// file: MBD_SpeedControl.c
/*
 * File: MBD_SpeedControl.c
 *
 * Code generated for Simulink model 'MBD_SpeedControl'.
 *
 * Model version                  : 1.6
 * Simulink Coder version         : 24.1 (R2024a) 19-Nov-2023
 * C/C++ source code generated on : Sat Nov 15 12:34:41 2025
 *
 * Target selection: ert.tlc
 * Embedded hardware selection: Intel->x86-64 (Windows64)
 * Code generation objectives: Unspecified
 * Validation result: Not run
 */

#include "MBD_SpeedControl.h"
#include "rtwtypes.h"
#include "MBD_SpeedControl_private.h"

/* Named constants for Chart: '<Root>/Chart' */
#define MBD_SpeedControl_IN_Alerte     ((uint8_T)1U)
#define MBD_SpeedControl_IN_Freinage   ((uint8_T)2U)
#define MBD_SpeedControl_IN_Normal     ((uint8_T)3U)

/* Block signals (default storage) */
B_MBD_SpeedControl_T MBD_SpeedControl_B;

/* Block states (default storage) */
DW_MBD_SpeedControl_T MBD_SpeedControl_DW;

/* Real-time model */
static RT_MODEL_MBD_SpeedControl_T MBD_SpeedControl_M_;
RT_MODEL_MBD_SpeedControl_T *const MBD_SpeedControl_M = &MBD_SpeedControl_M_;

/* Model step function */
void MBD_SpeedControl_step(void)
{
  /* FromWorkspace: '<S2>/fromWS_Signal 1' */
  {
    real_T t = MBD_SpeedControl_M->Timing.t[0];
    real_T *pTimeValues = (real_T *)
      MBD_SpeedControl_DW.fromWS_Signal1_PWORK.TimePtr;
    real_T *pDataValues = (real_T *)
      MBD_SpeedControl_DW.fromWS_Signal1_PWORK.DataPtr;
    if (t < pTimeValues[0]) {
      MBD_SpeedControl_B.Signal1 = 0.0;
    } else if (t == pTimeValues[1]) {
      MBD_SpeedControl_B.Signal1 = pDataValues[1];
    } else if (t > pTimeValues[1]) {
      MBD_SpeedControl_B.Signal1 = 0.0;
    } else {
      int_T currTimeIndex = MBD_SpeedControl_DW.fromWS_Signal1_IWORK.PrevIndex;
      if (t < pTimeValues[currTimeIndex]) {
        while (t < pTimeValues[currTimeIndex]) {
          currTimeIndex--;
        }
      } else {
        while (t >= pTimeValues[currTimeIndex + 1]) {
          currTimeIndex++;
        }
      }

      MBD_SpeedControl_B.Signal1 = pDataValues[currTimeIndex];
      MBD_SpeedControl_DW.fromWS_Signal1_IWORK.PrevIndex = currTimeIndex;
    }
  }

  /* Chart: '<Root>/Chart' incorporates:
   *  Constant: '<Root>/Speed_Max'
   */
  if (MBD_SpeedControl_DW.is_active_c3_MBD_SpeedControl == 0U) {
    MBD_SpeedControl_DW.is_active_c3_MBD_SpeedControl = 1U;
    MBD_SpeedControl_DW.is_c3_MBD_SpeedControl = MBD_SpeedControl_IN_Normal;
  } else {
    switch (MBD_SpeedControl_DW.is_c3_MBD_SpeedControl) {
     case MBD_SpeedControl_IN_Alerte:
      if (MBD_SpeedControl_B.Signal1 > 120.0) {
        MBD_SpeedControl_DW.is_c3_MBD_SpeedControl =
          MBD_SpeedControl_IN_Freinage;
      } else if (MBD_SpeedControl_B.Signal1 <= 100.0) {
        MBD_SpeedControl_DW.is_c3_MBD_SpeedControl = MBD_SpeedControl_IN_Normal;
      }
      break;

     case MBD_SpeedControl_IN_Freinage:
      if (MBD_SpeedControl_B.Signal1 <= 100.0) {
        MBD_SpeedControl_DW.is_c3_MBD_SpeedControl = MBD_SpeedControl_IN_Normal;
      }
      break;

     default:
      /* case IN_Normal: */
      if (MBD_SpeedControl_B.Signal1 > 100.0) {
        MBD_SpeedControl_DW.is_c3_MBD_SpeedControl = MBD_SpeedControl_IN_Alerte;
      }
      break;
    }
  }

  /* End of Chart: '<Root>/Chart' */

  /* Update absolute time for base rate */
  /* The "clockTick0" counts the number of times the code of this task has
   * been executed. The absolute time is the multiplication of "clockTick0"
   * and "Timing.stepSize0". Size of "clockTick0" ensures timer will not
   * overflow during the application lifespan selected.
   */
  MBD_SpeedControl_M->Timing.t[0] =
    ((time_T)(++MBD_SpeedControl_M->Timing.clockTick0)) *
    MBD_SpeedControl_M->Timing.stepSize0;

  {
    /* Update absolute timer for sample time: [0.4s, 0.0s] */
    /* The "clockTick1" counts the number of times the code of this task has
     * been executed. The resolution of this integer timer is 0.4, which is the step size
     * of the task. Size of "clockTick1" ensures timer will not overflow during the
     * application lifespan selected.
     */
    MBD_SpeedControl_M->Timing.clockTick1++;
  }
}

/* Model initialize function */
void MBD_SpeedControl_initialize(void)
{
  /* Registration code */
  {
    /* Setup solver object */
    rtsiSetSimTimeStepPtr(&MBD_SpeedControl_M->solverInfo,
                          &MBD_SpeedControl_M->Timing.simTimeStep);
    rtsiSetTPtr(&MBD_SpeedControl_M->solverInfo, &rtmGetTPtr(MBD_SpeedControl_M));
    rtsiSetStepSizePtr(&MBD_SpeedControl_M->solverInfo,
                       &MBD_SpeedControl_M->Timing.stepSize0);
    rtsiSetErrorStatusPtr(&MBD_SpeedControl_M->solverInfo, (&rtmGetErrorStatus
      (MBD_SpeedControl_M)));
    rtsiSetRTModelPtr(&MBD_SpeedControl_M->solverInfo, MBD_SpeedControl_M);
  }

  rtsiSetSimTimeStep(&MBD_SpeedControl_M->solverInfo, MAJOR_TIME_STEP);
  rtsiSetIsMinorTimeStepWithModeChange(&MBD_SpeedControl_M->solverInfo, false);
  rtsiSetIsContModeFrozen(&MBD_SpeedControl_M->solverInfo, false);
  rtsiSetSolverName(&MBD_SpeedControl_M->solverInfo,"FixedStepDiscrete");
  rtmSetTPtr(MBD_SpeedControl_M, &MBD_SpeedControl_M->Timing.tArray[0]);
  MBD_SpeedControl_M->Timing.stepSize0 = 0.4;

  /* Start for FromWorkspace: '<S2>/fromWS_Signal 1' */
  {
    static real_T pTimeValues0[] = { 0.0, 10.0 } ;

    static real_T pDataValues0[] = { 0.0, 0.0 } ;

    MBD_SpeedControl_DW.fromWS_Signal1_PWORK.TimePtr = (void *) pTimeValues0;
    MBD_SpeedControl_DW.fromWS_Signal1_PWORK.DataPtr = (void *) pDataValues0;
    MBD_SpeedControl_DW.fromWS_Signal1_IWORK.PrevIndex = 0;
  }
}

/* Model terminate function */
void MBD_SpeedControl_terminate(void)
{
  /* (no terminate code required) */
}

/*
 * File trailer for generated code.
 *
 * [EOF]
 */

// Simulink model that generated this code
simulink model "MBD_SpeedControl"  (R2024a)
settings: Solver=FixedStepDiscrete  StartTime=0.0  StopTime=20.0  RelTol=1e-3
libraries: SignalEditorBlockLib x1

== system MBD_SpeedControl ==
  Chart : Stateflow chart  TreatAsAtomicUnit=on
  Display : Display
  Display1 : Display
  Scope : Scope
  Scope1 : Scope
  Speed : SignalEditorBlockLib/Signal Editor  FileName=C:\Users\Hakima Ayed\Desktop\Vitesse\Speed.mat  ActiveScenario=Scenario  ActiveSignal=Signal 1  IsBus=off  OutputBusObjectStr=Bus: BusObject  SampleTime=0  Interpolate=off  ZeroCross=off  OutputAfterFinalValue=Setting to zero  Unit=inherit  PreserveSignalName=on  ApplySigPropsToAllScenarios=on  ApplySigPropsToAllSignals=off
  Speed_Max : Constant  Value=100
  wires:
  Speed_Max/1 -> Chart/2(Speed_Max)
  Chart/1(OverSpeed_Alert) -> Display1/1
  Chart/2(Brake_Command) -> Scope/1
  Speed/1 -> Scope1/1, Display/1, Chart/1(Speed)

== stateflow chart MBD_SpeedControl/Chart ==
  state Alerte
    OverSpeed_Alert = true;
    Brake_Command = false;
  state Freinage
    OverSpeed_Alert = true;
    Brake_Command = true;
  state Normal
    OverSpeed_Alert = false;
    Brake_Command=false;
  Normal -> Alerte : [Speed > Speed_Max
      | ]
  Alerte -> Freinage [order 1] : [Speed > Speed_Max + 20
      | ]
  Alerte -> Normal [order 2] : [Speed <= Speed_Max
      | ]
  (default) -> Normal
  Freinage -> Normal : [Speed <= Speed_Max
      | ]
  data: Speed input size=1; Speed_Max input size=1; OverSpeed_Alert output boolean size=1; Brake_Command output boolean size=1
